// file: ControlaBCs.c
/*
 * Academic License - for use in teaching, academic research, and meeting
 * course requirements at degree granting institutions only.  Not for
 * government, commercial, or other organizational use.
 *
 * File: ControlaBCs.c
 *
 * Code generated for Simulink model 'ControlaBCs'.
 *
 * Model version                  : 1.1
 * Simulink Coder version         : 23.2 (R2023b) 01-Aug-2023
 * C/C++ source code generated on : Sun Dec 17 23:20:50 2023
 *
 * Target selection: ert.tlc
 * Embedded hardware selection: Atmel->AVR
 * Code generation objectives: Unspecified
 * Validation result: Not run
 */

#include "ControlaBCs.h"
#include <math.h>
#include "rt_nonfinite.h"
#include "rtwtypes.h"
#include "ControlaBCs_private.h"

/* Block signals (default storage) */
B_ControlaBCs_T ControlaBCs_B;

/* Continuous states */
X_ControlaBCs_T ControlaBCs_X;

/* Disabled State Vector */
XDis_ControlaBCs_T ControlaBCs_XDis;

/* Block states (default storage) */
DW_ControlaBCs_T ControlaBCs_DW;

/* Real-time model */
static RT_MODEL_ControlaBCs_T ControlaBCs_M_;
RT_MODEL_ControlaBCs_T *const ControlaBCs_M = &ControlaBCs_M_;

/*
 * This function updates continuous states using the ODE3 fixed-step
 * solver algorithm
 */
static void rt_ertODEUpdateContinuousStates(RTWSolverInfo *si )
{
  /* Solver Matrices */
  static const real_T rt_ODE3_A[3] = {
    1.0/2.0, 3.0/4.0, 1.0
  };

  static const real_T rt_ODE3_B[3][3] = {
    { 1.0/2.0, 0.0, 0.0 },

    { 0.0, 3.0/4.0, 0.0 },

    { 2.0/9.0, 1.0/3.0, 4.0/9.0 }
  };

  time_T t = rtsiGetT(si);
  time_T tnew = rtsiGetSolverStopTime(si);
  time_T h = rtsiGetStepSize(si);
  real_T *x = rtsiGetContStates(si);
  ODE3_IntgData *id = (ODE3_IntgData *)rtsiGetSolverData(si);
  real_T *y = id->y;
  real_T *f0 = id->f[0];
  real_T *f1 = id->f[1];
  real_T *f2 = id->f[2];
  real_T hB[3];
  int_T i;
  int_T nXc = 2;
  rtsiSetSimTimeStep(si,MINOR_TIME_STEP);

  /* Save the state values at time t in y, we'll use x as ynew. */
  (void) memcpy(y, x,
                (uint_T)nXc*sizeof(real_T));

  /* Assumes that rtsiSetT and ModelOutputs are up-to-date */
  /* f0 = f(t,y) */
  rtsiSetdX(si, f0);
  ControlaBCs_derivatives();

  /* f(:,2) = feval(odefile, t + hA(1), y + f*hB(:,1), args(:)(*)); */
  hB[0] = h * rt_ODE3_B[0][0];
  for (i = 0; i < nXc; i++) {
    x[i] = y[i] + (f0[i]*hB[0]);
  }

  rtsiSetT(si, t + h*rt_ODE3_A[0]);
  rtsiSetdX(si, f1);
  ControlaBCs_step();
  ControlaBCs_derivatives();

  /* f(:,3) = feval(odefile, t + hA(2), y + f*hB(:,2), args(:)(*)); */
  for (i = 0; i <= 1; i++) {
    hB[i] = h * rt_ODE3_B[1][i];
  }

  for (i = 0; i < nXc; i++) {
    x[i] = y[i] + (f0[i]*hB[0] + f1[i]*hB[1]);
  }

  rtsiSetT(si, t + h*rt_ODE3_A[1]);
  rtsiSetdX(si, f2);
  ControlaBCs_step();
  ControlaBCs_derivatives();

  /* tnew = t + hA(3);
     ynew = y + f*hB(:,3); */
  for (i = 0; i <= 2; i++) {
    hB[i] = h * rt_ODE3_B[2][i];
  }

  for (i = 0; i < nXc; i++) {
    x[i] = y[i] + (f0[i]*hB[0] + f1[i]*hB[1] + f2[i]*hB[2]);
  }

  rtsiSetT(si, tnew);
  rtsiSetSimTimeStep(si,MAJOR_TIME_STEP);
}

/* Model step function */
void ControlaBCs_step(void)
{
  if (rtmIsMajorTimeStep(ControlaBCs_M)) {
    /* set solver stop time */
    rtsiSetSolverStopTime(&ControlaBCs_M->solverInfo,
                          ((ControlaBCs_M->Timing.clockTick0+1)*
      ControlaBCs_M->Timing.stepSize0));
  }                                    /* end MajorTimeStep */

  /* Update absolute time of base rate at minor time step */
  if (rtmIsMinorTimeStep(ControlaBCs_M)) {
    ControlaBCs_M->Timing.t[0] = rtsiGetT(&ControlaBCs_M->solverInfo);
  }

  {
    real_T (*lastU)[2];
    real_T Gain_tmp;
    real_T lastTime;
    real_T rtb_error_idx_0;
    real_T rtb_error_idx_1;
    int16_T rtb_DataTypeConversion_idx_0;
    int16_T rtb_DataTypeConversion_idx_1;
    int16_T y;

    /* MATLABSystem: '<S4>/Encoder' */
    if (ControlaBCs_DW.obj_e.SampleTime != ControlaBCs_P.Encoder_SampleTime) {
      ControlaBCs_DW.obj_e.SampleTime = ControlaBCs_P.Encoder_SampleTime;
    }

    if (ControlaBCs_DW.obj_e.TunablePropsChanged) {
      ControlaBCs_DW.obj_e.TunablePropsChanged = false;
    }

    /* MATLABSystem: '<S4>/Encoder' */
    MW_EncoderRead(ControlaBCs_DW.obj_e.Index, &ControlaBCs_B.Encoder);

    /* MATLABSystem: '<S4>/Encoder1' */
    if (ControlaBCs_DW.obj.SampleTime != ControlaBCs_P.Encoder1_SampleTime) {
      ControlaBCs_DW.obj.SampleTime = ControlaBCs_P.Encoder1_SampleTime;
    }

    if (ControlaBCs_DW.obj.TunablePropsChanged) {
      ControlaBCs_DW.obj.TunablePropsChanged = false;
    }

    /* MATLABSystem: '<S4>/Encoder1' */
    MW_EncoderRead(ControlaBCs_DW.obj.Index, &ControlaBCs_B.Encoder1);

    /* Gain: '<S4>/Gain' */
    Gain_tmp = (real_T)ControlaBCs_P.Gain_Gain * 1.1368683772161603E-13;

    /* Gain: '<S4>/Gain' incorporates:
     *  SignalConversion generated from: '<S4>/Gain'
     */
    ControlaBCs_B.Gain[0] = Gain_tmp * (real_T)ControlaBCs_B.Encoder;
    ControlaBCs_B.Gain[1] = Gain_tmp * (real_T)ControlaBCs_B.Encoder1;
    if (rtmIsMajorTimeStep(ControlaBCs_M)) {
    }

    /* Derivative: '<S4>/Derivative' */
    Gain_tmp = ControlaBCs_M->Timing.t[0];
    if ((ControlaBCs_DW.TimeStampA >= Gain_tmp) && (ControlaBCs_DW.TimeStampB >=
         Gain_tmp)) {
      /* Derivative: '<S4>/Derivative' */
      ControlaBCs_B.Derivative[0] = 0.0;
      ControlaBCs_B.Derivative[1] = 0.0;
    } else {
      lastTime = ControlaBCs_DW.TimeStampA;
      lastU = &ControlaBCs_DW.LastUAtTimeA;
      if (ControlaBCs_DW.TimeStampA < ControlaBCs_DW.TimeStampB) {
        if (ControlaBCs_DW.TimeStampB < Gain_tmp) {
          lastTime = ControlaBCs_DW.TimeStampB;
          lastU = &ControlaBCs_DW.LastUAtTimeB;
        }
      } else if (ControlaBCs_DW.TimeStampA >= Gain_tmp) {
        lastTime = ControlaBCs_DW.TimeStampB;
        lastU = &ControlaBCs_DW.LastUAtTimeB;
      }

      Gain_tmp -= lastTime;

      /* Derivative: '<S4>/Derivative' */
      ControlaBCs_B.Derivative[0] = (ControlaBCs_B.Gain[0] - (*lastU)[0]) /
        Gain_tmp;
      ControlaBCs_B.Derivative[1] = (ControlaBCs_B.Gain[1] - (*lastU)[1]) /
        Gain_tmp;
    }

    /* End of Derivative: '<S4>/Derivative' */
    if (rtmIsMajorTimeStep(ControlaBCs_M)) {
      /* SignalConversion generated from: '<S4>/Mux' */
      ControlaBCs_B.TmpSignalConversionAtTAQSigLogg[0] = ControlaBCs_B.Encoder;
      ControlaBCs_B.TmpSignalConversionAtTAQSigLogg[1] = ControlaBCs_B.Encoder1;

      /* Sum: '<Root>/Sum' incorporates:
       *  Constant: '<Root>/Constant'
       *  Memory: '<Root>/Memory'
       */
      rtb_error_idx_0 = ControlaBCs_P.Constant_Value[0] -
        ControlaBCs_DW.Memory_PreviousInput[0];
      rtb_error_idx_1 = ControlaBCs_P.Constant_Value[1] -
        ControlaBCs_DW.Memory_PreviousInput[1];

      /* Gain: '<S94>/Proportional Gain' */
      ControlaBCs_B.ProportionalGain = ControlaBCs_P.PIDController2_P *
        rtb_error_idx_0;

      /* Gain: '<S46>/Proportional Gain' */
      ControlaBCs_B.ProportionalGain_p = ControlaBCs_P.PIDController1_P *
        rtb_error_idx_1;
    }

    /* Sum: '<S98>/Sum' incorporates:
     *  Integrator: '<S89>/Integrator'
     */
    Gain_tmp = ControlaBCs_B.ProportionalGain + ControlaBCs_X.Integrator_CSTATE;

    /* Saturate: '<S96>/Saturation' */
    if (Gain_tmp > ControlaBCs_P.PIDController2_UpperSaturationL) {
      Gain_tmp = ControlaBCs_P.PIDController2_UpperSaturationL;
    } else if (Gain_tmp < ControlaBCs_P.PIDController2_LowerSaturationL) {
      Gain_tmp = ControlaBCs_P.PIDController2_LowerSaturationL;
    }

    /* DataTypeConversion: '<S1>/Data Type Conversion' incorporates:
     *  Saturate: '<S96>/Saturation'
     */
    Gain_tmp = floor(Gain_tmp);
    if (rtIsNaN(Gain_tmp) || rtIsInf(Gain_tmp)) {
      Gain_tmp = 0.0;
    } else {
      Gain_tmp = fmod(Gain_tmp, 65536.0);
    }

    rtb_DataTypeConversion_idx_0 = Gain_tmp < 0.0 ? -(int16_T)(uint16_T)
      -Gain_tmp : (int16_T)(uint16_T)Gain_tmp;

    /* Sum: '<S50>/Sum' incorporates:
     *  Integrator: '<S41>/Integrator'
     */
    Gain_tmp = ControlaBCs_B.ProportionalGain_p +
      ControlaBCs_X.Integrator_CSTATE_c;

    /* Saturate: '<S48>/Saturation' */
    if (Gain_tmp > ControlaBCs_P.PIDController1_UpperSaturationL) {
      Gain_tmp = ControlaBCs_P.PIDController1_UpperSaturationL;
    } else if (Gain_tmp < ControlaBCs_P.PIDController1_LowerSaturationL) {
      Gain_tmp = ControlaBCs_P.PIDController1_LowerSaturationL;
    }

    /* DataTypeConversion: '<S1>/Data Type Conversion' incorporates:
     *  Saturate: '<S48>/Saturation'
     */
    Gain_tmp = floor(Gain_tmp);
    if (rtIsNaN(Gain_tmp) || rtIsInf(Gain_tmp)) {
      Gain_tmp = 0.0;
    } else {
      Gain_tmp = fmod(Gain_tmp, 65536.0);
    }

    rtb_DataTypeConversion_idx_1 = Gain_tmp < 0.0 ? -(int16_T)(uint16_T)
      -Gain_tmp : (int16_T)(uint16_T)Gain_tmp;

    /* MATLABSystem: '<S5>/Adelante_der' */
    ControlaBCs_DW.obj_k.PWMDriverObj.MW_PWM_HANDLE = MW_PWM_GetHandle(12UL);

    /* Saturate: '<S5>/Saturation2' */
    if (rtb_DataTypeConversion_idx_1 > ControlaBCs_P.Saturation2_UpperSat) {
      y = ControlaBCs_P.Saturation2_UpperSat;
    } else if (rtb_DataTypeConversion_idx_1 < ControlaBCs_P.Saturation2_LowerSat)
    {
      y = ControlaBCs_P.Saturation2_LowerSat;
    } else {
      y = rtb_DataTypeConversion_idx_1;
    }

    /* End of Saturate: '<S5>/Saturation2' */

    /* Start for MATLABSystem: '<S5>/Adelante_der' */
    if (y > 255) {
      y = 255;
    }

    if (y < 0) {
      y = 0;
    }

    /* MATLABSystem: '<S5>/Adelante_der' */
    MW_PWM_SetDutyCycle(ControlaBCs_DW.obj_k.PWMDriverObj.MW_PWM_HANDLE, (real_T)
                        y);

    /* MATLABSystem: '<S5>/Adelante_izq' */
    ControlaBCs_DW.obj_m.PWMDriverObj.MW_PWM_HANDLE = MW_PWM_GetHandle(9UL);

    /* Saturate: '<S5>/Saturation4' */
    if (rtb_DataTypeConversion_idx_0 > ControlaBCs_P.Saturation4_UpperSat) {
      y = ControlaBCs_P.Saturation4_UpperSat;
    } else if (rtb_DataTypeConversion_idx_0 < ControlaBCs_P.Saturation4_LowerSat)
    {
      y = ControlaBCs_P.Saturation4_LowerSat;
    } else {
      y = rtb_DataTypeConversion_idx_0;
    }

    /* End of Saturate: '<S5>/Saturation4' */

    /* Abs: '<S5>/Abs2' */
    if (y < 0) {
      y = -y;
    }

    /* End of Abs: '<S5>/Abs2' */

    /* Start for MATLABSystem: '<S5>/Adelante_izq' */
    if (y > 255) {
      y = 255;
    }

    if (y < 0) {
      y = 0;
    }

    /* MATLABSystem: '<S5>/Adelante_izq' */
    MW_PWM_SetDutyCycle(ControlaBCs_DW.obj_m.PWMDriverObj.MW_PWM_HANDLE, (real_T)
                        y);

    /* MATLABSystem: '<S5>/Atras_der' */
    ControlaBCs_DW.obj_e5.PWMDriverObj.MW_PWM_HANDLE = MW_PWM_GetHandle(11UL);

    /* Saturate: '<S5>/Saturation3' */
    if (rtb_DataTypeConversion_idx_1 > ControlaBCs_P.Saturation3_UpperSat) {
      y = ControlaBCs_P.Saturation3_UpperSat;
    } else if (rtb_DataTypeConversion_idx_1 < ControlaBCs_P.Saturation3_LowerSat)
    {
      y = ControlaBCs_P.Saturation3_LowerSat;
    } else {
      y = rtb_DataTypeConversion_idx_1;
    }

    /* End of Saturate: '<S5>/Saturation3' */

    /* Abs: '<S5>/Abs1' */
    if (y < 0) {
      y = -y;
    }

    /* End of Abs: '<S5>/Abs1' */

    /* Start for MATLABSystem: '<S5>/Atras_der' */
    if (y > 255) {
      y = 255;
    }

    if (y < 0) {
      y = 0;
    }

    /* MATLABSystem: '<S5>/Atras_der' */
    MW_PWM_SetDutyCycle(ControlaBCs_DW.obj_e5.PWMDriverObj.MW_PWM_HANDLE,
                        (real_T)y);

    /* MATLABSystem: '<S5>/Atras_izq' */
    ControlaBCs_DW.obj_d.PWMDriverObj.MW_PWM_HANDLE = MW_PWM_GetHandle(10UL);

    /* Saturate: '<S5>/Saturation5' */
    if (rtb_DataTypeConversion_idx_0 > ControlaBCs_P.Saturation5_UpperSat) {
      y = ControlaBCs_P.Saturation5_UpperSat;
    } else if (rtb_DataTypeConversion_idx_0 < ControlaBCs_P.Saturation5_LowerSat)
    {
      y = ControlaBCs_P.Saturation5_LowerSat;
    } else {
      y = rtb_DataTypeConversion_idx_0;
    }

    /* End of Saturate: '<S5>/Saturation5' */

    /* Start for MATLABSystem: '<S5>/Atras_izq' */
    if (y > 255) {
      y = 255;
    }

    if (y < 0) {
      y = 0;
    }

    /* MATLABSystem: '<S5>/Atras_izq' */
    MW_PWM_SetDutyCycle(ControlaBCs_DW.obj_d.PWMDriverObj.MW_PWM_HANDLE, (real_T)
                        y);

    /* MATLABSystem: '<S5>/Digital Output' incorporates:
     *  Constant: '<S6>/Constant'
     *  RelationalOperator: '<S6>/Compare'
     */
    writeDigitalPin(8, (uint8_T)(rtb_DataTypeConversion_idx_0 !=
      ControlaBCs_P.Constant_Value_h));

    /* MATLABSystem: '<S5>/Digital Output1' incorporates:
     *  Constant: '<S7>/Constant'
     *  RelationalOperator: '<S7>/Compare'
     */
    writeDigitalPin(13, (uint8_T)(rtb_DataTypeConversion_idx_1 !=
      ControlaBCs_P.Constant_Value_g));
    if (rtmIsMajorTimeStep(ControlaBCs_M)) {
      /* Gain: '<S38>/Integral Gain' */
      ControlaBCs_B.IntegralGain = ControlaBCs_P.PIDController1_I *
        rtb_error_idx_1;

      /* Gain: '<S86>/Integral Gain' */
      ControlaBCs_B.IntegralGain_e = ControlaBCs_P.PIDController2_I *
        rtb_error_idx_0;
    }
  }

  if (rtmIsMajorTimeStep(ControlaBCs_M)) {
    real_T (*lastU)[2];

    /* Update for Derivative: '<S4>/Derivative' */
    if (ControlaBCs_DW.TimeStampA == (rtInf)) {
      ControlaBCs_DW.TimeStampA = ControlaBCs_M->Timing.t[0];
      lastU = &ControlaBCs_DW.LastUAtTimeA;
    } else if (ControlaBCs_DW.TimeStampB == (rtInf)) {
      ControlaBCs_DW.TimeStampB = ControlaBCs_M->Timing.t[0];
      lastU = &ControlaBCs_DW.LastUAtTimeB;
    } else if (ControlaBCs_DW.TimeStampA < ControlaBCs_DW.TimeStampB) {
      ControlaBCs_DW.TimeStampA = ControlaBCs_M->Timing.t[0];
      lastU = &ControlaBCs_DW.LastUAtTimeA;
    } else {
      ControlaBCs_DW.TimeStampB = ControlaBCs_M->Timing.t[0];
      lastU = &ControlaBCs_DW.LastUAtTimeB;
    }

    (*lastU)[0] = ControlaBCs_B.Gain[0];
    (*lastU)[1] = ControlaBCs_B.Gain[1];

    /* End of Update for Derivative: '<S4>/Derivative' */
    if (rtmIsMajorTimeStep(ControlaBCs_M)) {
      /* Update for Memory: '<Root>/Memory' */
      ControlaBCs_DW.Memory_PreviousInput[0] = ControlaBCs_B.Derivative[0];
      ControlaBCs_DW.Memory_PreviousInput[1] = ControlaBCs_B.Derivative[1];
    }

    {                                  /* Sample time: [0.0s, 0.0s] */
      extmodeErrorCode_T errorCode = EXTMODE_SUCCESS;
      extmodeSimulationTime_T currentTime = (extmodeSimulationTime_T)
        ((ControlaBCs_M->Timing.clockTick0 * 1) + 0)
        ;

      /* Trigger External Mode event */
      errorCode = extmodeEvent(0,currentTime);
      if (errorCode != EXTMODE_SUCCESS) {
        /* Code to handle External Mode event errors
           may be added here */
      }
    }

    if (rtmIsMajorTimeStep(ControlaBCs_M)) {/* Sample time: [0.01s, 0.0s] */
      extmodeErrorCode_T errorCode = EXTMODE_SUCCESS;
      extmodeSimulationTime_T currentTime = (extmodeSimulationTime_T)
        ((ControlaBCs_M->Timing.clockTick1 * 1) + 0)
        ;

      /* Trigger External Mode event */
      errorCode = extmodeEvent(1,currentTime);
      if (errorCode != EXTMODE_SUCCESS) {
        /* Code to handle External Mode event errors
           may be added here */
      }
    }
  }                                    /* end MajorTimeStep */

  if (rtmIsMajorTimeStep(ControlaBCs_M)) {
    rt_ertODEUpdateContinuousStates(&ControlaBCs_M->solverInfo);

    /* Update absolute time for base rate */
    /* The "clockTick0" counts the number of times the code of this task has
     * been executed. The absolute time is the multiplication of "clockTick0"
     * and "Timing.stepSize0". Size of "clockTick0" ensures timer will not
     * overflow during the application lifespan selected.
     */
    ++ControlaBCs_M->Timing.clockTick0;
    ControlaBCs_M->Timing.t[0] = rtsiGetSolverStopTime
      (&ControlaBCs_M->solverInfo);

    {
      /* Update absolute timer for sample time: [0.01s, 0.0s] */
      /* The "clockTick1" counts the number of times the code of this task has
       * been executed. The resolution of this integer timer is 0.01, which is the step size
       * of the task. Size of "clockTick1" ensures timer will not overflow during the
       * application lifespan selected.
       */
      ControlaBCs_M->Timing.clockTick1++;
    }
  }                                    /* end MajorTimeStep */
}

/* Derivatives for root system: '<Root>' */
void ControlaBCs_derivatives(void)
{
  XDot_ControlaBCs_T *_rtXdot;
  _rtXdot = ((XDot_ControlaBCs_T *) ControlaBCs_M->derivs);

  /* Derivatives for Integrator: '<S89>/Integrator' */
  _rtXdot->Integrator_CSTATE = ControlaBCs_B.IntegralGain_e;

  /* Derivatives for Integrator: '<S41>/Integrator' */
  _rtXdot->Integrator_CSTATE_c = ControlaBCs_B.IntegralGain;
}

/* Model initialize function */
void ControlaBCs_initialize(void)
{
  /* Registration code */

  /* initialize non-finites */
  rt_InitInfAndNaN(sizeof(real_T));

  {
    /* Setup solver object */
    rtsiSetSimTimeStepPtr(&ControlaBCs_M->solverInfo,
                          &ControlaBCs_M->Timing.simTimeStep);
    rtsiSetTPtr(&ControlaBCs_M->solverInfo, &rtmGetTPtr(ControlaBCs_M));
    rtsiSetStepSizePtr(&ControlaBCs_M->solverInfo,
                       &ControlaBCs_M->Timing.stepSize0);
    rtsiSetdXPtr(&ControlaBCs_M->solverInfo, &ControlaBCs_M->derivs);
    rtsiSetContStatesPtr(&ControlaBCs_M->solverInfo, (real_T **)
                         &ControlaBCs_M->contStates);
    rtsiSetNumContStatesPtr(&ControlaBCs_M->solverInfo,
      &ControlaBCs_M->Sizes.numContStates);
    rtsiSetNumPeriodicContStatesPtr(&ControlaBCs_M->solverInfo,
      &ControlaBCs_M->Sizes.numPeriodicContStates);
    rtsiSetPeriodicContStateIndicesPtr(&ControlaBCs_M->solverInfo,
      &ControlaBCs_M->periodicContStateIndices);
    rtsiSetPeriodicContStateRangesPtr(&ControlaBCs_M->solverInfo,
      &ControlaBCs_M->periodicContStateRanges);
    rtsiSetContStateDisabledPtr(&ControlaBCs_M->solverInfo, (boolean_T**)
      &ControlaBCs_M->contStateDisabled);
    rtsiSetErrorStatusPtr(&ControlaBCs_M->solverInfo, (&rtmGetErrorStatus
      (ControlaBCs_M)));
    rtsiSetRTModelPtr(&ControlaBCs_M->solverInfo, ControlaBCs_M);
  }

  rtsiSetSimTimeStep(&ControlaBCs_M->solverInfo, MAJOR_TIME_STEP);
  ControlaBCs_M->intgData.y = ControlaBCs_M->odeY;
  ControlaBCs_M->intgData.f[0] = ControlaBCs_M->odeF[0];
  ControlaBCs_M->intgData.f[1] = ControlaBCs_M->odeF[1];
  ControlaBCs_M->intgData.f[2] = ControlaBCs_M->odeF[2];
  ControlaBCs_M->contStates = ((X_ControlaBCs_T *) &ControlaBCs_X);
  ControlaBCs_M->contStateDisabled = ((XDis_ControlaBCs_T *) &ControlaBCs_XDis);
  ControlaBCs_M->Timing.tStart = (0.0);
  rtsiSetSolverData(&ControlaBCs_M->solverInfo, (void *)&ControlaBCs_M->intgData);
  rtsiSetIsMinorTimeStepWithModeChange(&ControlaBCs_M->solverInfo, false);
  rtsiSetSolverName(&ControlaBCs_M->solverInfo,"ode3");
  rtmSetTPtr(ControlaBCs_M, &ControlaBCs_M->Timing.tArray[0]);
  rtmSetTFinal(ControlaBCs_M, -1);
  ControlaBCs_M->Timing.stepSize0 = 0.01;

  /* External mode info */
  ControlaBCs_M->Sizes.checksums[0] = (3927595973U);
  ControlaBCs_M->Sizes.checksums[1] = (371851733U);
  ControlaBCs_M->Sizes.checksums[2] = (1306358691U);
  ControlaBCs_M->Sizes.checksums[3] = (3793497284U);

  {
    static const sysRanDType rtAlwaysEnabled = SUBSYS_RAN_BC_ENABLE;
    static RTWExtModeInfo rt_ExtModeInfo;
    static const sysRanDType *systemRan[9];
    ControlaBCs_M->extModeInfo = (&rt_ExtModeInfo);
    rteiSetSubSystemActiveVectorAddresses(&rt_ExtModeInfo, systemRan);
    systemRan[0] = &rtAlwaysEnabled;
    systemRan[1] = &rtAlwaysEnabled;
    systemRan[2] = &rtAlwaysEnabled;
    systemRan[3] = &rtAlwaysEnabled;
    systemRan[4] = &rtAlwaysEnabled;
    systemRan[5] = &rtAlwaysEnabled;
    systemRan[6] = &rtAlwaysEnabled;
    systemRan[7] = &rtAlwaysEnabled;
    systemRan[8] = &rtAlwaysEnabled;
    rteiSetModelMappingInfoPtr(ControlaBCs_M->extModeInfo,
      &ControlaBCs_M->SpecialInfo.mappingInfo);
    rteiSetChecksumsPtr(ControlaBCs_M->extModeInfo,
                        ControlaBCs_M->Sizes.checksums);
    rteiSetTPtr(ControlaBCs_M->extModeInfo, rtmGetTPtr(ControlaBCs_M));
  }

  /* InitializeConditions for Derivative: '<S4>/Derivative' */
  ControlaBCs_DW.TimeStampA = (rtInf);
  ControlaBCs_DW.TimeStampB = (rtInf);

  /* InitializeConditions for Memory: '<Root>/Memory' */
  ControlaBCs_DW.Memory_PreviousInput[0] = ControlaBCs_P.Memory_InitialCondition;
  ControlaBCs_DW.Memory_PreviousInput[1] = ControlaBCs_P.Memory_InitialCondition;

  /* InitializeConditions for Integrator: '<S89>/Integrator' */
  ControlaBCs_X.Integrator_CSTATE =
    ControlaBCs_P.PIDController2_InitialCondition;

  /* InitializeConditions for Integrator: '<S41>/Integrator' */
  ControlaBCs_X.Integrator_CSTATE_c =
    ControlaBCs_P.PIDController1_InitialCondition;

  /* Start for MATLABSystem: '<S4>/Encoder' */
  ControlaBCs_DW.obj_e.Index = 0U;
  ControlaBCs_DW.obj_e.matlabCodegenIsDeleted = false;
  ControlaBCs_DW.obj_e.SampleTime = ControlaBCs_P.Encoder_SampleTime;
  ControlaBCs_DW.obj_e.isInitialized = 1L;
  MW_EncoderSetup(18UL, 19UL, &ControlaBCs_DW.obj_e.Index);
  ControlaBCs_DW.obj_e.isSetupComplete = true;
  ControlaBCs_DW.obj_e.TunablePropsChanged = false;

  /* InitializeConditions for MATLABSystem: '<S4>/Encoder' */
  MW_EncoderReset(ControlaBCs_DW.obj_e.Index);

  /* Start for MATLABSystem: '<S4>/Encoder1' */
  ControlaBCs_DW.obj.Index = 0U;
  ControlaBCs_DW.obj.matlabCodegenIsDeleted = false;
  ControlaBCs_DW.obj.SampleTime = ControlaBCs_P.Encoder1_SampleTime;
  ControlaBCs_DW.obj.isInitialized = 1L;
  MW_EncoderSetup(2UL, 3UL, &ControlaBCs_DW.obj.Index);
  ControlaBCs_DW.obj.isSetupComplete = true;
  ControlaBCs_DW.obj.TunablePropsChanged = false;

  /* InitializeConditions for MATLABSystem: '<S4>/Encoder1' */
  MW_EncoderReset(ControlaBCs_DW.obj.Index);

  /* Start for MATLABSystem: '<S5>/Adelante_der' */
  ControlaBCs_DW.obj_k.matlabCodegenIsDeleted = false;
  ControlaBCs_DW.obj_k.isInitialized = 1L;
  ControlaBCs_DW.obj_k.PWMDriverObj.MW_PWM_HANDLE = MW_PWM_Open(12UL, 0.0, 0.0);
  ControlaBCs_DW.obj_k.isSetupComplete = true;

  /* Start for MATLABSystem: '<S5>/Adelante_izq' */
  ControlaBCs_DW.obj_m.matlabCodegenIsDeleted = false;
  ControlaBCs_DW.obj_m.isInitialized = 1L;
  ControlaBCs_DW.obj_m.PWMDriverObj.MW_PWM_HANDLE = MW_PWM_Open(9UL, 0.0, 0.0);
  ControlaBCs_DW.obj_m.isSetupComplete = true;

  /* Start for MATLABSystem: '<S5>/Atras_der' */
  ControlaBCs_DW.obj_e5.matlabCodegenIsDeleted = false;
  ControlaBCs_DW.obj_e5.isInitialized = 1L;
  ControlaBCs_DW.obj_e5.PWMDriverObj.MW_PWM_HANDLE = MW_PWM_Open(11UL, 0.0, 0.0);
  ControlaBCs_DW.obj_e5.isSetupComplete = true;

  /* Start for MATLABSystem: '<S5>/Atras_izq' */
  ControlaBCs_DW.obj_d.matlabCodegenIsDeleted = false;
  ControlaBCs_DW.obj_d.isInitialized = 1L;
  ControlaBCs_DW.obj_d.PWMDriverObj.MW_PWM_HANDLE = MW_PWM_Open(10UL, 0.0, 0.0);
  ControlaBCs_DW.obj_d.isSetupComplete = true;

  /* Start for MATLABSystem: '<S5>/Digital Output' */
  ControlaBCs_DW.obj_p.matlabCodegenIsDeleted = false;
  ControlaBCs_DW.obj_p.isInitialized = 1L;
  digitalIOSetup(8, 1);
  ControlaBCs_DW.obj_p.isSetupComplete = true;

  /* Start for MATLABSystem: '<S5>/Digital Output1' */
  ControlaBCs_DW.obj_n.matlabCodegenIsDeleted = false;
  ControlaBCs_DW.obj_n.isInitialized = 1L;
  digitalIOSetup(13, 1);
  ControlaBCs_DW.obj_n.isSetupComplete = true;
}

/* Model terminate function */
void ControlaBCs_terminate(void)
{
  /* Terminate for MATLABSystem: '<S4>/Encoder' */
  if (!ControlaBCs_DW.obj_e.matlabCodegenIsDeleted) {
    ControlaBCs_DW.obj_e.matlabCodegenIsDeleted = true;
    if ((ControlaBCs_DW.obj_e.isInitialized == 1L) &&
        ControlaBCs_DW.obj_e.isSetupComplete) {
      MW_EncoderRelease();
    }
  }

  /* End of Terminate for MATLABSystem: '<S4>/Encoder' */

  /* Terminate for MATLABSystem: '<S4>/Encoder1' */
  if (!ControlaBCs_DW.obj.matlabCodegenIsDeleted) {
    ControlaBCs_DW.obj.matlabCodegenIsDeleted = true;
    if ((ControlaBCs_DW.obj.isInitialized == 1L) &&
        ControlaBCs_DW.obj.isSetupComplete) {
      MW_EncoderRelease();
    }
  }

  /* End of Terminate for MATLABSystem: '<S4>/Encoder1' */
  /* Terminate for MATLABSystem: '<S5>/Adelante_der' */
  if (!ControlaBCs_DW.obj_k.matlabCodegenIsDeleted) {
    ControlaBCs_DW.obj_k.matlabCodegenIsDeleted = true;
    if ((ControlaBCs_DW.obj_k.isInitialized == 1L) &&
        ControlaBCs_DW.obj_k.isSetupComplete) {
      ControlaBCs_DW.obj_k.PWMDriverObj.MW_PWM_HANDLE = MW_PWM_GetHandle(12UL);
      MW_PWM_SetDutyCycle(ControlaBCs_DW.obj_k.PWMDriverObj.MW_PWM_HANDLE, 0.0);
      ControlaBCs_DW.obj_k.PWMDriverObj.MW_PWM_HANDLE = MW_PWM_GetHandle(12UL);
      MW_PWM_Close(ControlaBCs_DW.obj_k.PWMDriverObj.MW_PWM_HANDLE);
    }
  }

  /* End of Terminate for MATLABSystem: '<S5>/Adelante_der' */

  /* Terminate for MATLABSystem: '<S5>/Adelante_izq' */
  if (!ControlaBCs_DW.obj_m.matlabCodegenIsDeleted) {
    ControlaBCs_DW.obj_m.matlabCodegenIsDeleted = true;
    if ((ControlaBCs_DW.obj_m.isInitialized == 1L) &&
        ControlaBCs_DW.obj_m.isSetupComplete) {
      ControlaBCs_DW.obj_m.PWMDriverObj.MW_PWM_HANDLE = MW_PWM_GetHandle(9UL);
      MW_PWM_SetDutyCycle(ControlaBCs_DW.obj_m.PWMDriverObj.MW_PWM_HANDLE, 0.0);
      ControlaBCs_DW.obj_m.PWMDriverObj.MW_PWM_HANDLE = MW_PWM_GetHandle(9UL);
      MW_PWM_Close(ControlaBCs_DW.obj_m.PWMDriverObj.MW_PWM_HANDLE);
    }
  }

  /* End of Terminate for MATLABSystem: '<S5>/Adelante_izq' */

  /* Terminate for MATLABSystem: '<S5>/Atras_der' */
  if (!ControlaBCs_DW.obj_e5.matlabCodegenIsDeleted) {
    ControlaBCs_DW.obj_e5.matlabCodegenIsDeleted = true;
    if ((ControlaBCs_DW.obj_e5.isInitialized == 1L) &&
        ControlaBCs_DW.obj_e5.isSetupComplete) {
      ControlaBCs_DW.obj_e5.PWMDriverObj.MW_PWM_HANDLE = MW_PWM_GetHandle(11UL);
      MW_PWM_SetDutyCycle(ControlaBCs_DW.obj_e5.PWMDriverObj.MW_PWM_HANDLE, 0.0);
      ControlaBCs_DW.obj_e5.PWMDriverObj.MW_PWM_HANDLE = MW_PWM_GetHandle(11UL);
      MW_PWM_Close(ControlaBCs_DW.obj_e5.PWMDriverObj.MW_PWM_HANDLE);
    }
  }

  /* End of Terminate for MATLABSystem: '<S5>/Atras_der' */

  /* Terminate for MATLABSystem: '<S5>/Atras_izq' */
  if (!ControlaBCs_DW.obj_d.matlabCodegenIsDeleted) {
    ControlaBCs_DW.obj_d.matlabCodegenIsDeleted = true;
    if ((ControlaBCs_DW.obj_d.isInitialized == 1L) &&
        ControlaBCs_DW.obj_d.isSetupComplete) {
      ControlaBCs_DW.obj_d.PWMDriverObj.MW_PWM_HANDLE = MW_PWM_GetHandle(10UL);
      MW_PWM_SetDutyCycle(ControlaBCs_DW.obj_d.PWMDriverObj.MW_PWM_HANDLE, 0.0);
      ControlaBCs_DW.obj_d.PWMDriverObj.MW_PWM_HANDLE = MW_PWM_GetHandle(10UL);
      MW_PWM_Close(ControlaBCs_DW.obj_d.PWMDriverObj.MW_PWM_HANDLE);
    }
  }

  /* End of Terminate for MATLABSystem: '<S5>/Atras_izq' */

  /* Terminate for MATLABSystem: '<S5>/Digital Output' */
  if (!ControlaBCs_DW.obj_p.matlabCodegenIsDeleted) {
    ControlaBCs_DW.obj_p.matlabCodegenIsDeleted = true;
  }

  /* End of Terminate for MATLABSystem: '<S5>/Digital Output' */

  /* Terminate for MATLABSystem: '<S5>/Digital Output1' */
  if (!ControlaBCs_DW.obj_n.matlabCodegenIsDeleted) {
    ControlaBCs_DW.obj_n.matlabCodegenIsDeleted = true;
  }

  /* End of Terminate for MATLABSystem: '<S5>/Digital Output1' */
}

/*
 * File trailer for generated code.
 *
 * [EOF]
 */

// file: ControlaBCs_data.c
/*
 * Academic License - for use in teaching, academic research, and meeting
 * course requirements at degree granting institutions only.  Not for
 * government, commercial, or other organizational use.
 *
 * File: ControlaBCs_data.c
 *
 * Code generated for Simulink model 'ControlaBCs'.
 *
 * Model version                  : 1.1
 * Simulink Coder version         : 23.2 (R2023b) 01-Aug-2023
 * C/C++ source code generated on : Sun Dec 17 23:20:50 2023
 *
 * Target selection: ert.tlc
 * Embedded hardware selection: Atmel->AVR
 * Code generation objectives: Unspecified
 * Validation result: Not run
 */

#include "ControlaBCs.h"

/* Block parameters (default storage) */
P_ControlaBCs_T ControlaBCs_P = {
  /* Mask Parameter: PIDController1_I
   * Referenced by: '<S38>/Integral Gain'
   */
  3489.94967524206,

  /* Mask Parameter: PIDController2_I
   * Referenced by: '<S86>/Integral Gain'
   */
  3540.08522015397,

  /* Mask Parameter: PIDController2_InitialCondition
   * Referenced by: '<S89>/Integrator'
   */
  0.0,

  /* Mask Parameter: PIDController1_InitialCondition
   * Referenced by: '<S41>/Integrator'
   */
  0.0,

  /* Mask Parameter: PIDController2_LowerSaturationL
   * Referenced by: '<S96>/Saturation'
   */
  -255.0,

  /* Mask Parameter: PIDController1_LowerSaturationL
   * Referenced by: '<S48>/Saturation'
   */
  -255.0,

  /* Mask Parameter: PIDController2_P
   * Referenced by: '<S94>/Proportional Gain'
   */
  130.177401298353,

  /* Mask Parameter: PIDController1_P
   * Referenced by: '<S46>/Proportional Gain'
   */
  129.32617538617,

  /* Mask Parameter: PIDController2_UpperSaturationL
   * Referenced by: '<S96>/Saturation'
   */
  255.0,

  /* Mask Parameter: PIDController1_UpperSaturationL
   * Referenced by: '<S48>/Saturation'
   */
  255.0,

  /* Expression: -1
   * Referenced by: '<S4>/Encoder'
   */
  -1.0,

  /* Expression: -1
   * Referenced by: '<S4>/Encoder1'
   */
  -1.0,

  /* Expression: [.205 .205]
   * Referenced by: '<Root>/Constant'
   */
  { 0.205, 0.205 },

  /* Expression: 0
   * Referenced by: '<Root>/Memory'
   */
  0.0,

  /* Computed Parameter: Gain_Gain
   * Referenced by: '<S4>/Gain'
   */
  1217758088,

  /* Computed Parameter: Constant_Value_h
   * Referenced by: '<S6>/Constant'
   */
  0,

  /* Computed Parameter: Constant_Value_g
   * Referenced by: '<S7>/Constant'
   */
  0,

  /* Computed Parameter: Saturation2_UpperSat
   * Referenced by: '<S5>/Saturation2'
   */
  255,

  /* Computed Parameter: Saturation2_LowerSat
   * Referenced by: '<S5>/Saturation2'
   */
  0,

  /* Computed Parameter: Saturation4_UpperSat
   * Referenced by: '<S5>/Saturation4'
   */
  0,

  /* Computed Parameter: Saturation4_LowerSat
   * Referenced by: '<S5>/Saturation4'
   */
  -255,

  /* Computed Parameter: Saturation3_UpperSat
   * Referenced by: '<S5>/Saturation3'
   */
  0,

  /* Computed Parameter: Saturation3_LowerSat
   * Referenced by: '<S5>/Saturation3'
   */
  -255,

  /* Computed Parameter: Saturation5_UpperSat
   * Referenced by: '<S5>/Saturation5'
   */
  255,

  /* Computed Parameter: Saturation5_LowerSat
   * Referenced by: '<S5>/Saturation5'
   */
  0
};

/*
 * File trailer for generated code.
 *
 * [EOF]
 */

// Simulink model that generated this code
simulink model "ControlaBCs"  (R2023b)
settings: Solver=ode3  StartTime=0.0  StopTime=inf  FixedStep=0.01  RelTol=1e-3  EnableMultiTasking=on

== system ControlaBCs ==
  Constant : Constant  Value=[.205 .205]
  Display : Display
  Memory : Memory
  Planta : Subsystem  ReferencedSubsystem=Piero_Beltran_23
  Scope1 : Scope
  Subsystem Reference : Subsystem  ReferencedSubsystem=ControladorBCV2
  Sum : Sum  Inputs=|+-
  wires:
  Subsystem Reference/1 -> Planta/1  "pwm"
  Planta/1 -> Memory/1, Display/1, Scope1/1  "vel."
  Constant/1 -> Sum/1  "rel"
  Sum/1 -> Subsystem Reference/1  "error"
  Memory/1 -> Sum/2
